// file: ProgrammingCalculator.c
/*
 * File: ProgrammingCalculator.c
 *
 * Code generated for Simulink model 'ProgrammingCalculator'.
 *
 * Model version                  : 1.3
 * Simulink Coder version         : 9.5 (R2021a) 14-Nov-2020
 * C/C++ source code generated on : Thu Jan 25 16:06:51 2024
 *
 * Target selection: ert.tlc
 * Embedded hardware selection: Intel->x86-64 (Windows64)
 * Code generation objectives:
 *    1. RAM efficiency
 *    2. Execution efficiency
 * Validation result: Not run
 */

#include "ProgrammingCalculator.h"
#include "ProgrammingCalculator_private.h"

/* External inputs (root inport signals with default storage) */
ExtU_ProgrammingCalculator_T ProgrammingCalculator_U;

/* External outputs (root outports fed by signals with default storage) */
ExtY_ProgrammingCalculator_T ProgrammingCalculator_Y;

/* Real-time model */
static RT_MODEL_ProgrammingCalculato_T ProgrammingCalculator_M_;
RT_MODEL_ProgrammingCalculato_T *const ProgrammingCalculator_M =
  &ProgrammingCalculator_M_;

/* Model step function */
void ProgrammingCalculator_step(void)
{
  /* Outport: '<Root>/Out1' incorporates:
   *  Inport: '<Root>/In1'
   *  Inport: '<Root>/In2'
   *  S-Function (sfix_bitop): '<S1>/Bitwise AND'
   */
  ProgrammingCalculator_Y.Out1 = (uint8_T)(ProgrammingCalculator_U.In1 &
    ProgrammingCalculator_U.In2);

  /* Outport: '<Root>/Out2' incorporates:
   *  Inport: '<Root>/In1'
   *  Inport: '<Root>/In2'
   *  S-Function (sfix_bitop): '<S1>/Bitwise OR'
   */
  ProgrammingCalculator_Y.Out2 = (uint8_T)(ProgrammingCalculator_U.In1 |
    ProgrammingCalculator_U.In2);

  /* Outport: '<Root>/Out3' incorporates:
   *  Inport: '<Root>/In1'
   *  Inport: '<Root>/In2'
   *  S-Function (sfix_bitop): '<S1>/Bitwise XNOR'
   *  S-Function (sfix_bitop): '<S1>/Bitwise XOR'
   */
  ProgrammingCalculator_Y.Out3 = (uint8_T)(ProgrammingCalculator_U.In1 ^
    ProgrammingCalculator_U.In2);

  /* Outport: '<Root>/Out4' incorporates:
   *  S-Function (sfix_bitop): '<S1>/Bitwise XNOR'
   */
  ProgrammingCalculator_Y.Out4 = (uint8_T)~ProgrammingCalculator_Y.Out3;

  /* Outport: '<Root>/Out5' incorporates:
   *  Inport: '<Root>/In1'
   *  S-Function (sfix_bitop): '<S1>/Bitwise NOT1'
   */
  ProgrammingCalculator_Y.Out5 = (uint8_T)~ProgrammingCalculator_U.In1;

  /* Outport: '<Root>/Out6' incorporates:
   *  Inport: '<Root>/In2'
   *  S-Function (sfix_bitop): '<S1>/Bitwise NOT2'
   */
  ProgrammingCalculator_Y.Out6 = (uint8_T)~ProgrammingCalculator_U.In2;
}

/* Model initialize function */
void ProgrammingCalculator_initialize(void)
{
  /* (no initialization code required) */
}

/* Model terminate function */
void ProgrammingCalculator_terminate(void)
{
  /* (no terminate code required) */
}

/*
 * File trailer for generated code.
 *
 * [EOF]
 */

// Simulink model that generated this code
simulink model "ProgrammingCalculator"  (R2021a)
settings: Solver=FixedStepDiscrete  StartTime=0.0  StopTime=10.0  RelTol=1e-3
libraries: simulink x7

== system ProgrammingCalculator ==
  In1 : Inport  OutDataTypeStr=uint8
  In2 : Inport  Port=2  OutDataTypeStr=uint8
  Subsystem : Subsystem
  Out1 : Outport
  Out2 : Outport  Port=2
  Out3 : Outport  Port=3
  Out4 : Outport  Port=4
  Out5 : Outport  Port=5
  Out6 : Outport  Port=6
  wires:
  In1/1 -> Subsystem/1(In1)
  In2/1 -> Subsystem/2(In2)
  Subsystem/1(Out1) -> Out1/1
  Subsystem/2(Out2) -> Out2/1
  Subsystem/3(Out3) -> Out3/1
  Subsystem/4(Out4) -> Out4/1
  Subsystem/5(Out5) -> Out5/1
  Subsystem/6(Out6) -> Out6/1

== system ProgrammingCalculator/Subsystem ==
  In1 : Inport
  In2 : Inport  Port=2
  Bitwise AND : simulink/Logic and Bit Operations/Bitwise Operator  logicop=AND  UseBitMask=off  NumInputPorts=2  BitMask=bin2dec('11011001')  BitMaskRealWorld=Stored Integer
  Bitwise NOT1 : simulink/Logic and Bit Operations/Bitwise Operator  logicop=NOT  UseBitMask=off  BitMask=bin2dec('11011001')  BitMaskRealWorld=Stored Integer
  Bitwise NOT2 : simulink/Logic and Bit Operations/Bitwise Operator  logicop=NOT  UseBitMask=off  BitMask=bin2dec('11011001')  BitMaskRealWorld=Stored Integer
  Bitwise OR : simulink/Logic and Bit Operations/Bitwise Operator  logicop=OR  UseBitMask=off  NumInputPorts=2  BitMask=bin2dec('11011001')  BitMaskRealWorld=Stored Integer
  Bitwise XNOR : simulink/Logic and Bit Operations/Bitwise Operator  logicop=NOT  UseBitMask=off  BitMask=bin2dec('11011001')  BitMaskRealWorld=Stored Integer
  Bitwise XOR : simulink/Logic and Bit Operations/Bitwise Operator  logicop=XOR  UseBitMask=off  NumInputPorts=2  BitMask=bin2dec('11011001')  BitMaskRealWorld=Stored Integer
  Bitwise XOR2 : simulink/Logic and Bit Operations/Bitwise Operator  logicop=XOR  UseBitMask=off  NumInputPorts=2  BitMask=bin2dec('11011001')  BitMaskRealWorld=Stored Integer
  Out1 : Outport
  Out2 : Outport  Port=2
  Out3 : Outport  Port=3
  Out4 : Outport  Port=4
  Out5 : Outport  Port=5
  Out6 : Outport  Port=6
  wires:
  In2/1 -> Bitwise NOT2/1, Bitwise XOR2/2, Bitwise XOR/2, Bitwise OR/2, Bitwise AND/2
  In1/1 -> Bitwise NOT1/1, Bitwise XOR2/1, Bitwise XOR/1, Bitwise OR/1, Bitwise AND/1
  Bitwise AND/1 -> Out1/1
  Bitwise NOT1/1 -> Out5/1
  Bitwise OR/1 -> Out2/1
  Bitwise XNOR/1 -> Out4/1
  Bitwise NOT2/1 -> Out6/1
  Bitwise XOR/1 -> Out3/1
  Bitwise XOR2/1 -> Bitwise XNOR/1
